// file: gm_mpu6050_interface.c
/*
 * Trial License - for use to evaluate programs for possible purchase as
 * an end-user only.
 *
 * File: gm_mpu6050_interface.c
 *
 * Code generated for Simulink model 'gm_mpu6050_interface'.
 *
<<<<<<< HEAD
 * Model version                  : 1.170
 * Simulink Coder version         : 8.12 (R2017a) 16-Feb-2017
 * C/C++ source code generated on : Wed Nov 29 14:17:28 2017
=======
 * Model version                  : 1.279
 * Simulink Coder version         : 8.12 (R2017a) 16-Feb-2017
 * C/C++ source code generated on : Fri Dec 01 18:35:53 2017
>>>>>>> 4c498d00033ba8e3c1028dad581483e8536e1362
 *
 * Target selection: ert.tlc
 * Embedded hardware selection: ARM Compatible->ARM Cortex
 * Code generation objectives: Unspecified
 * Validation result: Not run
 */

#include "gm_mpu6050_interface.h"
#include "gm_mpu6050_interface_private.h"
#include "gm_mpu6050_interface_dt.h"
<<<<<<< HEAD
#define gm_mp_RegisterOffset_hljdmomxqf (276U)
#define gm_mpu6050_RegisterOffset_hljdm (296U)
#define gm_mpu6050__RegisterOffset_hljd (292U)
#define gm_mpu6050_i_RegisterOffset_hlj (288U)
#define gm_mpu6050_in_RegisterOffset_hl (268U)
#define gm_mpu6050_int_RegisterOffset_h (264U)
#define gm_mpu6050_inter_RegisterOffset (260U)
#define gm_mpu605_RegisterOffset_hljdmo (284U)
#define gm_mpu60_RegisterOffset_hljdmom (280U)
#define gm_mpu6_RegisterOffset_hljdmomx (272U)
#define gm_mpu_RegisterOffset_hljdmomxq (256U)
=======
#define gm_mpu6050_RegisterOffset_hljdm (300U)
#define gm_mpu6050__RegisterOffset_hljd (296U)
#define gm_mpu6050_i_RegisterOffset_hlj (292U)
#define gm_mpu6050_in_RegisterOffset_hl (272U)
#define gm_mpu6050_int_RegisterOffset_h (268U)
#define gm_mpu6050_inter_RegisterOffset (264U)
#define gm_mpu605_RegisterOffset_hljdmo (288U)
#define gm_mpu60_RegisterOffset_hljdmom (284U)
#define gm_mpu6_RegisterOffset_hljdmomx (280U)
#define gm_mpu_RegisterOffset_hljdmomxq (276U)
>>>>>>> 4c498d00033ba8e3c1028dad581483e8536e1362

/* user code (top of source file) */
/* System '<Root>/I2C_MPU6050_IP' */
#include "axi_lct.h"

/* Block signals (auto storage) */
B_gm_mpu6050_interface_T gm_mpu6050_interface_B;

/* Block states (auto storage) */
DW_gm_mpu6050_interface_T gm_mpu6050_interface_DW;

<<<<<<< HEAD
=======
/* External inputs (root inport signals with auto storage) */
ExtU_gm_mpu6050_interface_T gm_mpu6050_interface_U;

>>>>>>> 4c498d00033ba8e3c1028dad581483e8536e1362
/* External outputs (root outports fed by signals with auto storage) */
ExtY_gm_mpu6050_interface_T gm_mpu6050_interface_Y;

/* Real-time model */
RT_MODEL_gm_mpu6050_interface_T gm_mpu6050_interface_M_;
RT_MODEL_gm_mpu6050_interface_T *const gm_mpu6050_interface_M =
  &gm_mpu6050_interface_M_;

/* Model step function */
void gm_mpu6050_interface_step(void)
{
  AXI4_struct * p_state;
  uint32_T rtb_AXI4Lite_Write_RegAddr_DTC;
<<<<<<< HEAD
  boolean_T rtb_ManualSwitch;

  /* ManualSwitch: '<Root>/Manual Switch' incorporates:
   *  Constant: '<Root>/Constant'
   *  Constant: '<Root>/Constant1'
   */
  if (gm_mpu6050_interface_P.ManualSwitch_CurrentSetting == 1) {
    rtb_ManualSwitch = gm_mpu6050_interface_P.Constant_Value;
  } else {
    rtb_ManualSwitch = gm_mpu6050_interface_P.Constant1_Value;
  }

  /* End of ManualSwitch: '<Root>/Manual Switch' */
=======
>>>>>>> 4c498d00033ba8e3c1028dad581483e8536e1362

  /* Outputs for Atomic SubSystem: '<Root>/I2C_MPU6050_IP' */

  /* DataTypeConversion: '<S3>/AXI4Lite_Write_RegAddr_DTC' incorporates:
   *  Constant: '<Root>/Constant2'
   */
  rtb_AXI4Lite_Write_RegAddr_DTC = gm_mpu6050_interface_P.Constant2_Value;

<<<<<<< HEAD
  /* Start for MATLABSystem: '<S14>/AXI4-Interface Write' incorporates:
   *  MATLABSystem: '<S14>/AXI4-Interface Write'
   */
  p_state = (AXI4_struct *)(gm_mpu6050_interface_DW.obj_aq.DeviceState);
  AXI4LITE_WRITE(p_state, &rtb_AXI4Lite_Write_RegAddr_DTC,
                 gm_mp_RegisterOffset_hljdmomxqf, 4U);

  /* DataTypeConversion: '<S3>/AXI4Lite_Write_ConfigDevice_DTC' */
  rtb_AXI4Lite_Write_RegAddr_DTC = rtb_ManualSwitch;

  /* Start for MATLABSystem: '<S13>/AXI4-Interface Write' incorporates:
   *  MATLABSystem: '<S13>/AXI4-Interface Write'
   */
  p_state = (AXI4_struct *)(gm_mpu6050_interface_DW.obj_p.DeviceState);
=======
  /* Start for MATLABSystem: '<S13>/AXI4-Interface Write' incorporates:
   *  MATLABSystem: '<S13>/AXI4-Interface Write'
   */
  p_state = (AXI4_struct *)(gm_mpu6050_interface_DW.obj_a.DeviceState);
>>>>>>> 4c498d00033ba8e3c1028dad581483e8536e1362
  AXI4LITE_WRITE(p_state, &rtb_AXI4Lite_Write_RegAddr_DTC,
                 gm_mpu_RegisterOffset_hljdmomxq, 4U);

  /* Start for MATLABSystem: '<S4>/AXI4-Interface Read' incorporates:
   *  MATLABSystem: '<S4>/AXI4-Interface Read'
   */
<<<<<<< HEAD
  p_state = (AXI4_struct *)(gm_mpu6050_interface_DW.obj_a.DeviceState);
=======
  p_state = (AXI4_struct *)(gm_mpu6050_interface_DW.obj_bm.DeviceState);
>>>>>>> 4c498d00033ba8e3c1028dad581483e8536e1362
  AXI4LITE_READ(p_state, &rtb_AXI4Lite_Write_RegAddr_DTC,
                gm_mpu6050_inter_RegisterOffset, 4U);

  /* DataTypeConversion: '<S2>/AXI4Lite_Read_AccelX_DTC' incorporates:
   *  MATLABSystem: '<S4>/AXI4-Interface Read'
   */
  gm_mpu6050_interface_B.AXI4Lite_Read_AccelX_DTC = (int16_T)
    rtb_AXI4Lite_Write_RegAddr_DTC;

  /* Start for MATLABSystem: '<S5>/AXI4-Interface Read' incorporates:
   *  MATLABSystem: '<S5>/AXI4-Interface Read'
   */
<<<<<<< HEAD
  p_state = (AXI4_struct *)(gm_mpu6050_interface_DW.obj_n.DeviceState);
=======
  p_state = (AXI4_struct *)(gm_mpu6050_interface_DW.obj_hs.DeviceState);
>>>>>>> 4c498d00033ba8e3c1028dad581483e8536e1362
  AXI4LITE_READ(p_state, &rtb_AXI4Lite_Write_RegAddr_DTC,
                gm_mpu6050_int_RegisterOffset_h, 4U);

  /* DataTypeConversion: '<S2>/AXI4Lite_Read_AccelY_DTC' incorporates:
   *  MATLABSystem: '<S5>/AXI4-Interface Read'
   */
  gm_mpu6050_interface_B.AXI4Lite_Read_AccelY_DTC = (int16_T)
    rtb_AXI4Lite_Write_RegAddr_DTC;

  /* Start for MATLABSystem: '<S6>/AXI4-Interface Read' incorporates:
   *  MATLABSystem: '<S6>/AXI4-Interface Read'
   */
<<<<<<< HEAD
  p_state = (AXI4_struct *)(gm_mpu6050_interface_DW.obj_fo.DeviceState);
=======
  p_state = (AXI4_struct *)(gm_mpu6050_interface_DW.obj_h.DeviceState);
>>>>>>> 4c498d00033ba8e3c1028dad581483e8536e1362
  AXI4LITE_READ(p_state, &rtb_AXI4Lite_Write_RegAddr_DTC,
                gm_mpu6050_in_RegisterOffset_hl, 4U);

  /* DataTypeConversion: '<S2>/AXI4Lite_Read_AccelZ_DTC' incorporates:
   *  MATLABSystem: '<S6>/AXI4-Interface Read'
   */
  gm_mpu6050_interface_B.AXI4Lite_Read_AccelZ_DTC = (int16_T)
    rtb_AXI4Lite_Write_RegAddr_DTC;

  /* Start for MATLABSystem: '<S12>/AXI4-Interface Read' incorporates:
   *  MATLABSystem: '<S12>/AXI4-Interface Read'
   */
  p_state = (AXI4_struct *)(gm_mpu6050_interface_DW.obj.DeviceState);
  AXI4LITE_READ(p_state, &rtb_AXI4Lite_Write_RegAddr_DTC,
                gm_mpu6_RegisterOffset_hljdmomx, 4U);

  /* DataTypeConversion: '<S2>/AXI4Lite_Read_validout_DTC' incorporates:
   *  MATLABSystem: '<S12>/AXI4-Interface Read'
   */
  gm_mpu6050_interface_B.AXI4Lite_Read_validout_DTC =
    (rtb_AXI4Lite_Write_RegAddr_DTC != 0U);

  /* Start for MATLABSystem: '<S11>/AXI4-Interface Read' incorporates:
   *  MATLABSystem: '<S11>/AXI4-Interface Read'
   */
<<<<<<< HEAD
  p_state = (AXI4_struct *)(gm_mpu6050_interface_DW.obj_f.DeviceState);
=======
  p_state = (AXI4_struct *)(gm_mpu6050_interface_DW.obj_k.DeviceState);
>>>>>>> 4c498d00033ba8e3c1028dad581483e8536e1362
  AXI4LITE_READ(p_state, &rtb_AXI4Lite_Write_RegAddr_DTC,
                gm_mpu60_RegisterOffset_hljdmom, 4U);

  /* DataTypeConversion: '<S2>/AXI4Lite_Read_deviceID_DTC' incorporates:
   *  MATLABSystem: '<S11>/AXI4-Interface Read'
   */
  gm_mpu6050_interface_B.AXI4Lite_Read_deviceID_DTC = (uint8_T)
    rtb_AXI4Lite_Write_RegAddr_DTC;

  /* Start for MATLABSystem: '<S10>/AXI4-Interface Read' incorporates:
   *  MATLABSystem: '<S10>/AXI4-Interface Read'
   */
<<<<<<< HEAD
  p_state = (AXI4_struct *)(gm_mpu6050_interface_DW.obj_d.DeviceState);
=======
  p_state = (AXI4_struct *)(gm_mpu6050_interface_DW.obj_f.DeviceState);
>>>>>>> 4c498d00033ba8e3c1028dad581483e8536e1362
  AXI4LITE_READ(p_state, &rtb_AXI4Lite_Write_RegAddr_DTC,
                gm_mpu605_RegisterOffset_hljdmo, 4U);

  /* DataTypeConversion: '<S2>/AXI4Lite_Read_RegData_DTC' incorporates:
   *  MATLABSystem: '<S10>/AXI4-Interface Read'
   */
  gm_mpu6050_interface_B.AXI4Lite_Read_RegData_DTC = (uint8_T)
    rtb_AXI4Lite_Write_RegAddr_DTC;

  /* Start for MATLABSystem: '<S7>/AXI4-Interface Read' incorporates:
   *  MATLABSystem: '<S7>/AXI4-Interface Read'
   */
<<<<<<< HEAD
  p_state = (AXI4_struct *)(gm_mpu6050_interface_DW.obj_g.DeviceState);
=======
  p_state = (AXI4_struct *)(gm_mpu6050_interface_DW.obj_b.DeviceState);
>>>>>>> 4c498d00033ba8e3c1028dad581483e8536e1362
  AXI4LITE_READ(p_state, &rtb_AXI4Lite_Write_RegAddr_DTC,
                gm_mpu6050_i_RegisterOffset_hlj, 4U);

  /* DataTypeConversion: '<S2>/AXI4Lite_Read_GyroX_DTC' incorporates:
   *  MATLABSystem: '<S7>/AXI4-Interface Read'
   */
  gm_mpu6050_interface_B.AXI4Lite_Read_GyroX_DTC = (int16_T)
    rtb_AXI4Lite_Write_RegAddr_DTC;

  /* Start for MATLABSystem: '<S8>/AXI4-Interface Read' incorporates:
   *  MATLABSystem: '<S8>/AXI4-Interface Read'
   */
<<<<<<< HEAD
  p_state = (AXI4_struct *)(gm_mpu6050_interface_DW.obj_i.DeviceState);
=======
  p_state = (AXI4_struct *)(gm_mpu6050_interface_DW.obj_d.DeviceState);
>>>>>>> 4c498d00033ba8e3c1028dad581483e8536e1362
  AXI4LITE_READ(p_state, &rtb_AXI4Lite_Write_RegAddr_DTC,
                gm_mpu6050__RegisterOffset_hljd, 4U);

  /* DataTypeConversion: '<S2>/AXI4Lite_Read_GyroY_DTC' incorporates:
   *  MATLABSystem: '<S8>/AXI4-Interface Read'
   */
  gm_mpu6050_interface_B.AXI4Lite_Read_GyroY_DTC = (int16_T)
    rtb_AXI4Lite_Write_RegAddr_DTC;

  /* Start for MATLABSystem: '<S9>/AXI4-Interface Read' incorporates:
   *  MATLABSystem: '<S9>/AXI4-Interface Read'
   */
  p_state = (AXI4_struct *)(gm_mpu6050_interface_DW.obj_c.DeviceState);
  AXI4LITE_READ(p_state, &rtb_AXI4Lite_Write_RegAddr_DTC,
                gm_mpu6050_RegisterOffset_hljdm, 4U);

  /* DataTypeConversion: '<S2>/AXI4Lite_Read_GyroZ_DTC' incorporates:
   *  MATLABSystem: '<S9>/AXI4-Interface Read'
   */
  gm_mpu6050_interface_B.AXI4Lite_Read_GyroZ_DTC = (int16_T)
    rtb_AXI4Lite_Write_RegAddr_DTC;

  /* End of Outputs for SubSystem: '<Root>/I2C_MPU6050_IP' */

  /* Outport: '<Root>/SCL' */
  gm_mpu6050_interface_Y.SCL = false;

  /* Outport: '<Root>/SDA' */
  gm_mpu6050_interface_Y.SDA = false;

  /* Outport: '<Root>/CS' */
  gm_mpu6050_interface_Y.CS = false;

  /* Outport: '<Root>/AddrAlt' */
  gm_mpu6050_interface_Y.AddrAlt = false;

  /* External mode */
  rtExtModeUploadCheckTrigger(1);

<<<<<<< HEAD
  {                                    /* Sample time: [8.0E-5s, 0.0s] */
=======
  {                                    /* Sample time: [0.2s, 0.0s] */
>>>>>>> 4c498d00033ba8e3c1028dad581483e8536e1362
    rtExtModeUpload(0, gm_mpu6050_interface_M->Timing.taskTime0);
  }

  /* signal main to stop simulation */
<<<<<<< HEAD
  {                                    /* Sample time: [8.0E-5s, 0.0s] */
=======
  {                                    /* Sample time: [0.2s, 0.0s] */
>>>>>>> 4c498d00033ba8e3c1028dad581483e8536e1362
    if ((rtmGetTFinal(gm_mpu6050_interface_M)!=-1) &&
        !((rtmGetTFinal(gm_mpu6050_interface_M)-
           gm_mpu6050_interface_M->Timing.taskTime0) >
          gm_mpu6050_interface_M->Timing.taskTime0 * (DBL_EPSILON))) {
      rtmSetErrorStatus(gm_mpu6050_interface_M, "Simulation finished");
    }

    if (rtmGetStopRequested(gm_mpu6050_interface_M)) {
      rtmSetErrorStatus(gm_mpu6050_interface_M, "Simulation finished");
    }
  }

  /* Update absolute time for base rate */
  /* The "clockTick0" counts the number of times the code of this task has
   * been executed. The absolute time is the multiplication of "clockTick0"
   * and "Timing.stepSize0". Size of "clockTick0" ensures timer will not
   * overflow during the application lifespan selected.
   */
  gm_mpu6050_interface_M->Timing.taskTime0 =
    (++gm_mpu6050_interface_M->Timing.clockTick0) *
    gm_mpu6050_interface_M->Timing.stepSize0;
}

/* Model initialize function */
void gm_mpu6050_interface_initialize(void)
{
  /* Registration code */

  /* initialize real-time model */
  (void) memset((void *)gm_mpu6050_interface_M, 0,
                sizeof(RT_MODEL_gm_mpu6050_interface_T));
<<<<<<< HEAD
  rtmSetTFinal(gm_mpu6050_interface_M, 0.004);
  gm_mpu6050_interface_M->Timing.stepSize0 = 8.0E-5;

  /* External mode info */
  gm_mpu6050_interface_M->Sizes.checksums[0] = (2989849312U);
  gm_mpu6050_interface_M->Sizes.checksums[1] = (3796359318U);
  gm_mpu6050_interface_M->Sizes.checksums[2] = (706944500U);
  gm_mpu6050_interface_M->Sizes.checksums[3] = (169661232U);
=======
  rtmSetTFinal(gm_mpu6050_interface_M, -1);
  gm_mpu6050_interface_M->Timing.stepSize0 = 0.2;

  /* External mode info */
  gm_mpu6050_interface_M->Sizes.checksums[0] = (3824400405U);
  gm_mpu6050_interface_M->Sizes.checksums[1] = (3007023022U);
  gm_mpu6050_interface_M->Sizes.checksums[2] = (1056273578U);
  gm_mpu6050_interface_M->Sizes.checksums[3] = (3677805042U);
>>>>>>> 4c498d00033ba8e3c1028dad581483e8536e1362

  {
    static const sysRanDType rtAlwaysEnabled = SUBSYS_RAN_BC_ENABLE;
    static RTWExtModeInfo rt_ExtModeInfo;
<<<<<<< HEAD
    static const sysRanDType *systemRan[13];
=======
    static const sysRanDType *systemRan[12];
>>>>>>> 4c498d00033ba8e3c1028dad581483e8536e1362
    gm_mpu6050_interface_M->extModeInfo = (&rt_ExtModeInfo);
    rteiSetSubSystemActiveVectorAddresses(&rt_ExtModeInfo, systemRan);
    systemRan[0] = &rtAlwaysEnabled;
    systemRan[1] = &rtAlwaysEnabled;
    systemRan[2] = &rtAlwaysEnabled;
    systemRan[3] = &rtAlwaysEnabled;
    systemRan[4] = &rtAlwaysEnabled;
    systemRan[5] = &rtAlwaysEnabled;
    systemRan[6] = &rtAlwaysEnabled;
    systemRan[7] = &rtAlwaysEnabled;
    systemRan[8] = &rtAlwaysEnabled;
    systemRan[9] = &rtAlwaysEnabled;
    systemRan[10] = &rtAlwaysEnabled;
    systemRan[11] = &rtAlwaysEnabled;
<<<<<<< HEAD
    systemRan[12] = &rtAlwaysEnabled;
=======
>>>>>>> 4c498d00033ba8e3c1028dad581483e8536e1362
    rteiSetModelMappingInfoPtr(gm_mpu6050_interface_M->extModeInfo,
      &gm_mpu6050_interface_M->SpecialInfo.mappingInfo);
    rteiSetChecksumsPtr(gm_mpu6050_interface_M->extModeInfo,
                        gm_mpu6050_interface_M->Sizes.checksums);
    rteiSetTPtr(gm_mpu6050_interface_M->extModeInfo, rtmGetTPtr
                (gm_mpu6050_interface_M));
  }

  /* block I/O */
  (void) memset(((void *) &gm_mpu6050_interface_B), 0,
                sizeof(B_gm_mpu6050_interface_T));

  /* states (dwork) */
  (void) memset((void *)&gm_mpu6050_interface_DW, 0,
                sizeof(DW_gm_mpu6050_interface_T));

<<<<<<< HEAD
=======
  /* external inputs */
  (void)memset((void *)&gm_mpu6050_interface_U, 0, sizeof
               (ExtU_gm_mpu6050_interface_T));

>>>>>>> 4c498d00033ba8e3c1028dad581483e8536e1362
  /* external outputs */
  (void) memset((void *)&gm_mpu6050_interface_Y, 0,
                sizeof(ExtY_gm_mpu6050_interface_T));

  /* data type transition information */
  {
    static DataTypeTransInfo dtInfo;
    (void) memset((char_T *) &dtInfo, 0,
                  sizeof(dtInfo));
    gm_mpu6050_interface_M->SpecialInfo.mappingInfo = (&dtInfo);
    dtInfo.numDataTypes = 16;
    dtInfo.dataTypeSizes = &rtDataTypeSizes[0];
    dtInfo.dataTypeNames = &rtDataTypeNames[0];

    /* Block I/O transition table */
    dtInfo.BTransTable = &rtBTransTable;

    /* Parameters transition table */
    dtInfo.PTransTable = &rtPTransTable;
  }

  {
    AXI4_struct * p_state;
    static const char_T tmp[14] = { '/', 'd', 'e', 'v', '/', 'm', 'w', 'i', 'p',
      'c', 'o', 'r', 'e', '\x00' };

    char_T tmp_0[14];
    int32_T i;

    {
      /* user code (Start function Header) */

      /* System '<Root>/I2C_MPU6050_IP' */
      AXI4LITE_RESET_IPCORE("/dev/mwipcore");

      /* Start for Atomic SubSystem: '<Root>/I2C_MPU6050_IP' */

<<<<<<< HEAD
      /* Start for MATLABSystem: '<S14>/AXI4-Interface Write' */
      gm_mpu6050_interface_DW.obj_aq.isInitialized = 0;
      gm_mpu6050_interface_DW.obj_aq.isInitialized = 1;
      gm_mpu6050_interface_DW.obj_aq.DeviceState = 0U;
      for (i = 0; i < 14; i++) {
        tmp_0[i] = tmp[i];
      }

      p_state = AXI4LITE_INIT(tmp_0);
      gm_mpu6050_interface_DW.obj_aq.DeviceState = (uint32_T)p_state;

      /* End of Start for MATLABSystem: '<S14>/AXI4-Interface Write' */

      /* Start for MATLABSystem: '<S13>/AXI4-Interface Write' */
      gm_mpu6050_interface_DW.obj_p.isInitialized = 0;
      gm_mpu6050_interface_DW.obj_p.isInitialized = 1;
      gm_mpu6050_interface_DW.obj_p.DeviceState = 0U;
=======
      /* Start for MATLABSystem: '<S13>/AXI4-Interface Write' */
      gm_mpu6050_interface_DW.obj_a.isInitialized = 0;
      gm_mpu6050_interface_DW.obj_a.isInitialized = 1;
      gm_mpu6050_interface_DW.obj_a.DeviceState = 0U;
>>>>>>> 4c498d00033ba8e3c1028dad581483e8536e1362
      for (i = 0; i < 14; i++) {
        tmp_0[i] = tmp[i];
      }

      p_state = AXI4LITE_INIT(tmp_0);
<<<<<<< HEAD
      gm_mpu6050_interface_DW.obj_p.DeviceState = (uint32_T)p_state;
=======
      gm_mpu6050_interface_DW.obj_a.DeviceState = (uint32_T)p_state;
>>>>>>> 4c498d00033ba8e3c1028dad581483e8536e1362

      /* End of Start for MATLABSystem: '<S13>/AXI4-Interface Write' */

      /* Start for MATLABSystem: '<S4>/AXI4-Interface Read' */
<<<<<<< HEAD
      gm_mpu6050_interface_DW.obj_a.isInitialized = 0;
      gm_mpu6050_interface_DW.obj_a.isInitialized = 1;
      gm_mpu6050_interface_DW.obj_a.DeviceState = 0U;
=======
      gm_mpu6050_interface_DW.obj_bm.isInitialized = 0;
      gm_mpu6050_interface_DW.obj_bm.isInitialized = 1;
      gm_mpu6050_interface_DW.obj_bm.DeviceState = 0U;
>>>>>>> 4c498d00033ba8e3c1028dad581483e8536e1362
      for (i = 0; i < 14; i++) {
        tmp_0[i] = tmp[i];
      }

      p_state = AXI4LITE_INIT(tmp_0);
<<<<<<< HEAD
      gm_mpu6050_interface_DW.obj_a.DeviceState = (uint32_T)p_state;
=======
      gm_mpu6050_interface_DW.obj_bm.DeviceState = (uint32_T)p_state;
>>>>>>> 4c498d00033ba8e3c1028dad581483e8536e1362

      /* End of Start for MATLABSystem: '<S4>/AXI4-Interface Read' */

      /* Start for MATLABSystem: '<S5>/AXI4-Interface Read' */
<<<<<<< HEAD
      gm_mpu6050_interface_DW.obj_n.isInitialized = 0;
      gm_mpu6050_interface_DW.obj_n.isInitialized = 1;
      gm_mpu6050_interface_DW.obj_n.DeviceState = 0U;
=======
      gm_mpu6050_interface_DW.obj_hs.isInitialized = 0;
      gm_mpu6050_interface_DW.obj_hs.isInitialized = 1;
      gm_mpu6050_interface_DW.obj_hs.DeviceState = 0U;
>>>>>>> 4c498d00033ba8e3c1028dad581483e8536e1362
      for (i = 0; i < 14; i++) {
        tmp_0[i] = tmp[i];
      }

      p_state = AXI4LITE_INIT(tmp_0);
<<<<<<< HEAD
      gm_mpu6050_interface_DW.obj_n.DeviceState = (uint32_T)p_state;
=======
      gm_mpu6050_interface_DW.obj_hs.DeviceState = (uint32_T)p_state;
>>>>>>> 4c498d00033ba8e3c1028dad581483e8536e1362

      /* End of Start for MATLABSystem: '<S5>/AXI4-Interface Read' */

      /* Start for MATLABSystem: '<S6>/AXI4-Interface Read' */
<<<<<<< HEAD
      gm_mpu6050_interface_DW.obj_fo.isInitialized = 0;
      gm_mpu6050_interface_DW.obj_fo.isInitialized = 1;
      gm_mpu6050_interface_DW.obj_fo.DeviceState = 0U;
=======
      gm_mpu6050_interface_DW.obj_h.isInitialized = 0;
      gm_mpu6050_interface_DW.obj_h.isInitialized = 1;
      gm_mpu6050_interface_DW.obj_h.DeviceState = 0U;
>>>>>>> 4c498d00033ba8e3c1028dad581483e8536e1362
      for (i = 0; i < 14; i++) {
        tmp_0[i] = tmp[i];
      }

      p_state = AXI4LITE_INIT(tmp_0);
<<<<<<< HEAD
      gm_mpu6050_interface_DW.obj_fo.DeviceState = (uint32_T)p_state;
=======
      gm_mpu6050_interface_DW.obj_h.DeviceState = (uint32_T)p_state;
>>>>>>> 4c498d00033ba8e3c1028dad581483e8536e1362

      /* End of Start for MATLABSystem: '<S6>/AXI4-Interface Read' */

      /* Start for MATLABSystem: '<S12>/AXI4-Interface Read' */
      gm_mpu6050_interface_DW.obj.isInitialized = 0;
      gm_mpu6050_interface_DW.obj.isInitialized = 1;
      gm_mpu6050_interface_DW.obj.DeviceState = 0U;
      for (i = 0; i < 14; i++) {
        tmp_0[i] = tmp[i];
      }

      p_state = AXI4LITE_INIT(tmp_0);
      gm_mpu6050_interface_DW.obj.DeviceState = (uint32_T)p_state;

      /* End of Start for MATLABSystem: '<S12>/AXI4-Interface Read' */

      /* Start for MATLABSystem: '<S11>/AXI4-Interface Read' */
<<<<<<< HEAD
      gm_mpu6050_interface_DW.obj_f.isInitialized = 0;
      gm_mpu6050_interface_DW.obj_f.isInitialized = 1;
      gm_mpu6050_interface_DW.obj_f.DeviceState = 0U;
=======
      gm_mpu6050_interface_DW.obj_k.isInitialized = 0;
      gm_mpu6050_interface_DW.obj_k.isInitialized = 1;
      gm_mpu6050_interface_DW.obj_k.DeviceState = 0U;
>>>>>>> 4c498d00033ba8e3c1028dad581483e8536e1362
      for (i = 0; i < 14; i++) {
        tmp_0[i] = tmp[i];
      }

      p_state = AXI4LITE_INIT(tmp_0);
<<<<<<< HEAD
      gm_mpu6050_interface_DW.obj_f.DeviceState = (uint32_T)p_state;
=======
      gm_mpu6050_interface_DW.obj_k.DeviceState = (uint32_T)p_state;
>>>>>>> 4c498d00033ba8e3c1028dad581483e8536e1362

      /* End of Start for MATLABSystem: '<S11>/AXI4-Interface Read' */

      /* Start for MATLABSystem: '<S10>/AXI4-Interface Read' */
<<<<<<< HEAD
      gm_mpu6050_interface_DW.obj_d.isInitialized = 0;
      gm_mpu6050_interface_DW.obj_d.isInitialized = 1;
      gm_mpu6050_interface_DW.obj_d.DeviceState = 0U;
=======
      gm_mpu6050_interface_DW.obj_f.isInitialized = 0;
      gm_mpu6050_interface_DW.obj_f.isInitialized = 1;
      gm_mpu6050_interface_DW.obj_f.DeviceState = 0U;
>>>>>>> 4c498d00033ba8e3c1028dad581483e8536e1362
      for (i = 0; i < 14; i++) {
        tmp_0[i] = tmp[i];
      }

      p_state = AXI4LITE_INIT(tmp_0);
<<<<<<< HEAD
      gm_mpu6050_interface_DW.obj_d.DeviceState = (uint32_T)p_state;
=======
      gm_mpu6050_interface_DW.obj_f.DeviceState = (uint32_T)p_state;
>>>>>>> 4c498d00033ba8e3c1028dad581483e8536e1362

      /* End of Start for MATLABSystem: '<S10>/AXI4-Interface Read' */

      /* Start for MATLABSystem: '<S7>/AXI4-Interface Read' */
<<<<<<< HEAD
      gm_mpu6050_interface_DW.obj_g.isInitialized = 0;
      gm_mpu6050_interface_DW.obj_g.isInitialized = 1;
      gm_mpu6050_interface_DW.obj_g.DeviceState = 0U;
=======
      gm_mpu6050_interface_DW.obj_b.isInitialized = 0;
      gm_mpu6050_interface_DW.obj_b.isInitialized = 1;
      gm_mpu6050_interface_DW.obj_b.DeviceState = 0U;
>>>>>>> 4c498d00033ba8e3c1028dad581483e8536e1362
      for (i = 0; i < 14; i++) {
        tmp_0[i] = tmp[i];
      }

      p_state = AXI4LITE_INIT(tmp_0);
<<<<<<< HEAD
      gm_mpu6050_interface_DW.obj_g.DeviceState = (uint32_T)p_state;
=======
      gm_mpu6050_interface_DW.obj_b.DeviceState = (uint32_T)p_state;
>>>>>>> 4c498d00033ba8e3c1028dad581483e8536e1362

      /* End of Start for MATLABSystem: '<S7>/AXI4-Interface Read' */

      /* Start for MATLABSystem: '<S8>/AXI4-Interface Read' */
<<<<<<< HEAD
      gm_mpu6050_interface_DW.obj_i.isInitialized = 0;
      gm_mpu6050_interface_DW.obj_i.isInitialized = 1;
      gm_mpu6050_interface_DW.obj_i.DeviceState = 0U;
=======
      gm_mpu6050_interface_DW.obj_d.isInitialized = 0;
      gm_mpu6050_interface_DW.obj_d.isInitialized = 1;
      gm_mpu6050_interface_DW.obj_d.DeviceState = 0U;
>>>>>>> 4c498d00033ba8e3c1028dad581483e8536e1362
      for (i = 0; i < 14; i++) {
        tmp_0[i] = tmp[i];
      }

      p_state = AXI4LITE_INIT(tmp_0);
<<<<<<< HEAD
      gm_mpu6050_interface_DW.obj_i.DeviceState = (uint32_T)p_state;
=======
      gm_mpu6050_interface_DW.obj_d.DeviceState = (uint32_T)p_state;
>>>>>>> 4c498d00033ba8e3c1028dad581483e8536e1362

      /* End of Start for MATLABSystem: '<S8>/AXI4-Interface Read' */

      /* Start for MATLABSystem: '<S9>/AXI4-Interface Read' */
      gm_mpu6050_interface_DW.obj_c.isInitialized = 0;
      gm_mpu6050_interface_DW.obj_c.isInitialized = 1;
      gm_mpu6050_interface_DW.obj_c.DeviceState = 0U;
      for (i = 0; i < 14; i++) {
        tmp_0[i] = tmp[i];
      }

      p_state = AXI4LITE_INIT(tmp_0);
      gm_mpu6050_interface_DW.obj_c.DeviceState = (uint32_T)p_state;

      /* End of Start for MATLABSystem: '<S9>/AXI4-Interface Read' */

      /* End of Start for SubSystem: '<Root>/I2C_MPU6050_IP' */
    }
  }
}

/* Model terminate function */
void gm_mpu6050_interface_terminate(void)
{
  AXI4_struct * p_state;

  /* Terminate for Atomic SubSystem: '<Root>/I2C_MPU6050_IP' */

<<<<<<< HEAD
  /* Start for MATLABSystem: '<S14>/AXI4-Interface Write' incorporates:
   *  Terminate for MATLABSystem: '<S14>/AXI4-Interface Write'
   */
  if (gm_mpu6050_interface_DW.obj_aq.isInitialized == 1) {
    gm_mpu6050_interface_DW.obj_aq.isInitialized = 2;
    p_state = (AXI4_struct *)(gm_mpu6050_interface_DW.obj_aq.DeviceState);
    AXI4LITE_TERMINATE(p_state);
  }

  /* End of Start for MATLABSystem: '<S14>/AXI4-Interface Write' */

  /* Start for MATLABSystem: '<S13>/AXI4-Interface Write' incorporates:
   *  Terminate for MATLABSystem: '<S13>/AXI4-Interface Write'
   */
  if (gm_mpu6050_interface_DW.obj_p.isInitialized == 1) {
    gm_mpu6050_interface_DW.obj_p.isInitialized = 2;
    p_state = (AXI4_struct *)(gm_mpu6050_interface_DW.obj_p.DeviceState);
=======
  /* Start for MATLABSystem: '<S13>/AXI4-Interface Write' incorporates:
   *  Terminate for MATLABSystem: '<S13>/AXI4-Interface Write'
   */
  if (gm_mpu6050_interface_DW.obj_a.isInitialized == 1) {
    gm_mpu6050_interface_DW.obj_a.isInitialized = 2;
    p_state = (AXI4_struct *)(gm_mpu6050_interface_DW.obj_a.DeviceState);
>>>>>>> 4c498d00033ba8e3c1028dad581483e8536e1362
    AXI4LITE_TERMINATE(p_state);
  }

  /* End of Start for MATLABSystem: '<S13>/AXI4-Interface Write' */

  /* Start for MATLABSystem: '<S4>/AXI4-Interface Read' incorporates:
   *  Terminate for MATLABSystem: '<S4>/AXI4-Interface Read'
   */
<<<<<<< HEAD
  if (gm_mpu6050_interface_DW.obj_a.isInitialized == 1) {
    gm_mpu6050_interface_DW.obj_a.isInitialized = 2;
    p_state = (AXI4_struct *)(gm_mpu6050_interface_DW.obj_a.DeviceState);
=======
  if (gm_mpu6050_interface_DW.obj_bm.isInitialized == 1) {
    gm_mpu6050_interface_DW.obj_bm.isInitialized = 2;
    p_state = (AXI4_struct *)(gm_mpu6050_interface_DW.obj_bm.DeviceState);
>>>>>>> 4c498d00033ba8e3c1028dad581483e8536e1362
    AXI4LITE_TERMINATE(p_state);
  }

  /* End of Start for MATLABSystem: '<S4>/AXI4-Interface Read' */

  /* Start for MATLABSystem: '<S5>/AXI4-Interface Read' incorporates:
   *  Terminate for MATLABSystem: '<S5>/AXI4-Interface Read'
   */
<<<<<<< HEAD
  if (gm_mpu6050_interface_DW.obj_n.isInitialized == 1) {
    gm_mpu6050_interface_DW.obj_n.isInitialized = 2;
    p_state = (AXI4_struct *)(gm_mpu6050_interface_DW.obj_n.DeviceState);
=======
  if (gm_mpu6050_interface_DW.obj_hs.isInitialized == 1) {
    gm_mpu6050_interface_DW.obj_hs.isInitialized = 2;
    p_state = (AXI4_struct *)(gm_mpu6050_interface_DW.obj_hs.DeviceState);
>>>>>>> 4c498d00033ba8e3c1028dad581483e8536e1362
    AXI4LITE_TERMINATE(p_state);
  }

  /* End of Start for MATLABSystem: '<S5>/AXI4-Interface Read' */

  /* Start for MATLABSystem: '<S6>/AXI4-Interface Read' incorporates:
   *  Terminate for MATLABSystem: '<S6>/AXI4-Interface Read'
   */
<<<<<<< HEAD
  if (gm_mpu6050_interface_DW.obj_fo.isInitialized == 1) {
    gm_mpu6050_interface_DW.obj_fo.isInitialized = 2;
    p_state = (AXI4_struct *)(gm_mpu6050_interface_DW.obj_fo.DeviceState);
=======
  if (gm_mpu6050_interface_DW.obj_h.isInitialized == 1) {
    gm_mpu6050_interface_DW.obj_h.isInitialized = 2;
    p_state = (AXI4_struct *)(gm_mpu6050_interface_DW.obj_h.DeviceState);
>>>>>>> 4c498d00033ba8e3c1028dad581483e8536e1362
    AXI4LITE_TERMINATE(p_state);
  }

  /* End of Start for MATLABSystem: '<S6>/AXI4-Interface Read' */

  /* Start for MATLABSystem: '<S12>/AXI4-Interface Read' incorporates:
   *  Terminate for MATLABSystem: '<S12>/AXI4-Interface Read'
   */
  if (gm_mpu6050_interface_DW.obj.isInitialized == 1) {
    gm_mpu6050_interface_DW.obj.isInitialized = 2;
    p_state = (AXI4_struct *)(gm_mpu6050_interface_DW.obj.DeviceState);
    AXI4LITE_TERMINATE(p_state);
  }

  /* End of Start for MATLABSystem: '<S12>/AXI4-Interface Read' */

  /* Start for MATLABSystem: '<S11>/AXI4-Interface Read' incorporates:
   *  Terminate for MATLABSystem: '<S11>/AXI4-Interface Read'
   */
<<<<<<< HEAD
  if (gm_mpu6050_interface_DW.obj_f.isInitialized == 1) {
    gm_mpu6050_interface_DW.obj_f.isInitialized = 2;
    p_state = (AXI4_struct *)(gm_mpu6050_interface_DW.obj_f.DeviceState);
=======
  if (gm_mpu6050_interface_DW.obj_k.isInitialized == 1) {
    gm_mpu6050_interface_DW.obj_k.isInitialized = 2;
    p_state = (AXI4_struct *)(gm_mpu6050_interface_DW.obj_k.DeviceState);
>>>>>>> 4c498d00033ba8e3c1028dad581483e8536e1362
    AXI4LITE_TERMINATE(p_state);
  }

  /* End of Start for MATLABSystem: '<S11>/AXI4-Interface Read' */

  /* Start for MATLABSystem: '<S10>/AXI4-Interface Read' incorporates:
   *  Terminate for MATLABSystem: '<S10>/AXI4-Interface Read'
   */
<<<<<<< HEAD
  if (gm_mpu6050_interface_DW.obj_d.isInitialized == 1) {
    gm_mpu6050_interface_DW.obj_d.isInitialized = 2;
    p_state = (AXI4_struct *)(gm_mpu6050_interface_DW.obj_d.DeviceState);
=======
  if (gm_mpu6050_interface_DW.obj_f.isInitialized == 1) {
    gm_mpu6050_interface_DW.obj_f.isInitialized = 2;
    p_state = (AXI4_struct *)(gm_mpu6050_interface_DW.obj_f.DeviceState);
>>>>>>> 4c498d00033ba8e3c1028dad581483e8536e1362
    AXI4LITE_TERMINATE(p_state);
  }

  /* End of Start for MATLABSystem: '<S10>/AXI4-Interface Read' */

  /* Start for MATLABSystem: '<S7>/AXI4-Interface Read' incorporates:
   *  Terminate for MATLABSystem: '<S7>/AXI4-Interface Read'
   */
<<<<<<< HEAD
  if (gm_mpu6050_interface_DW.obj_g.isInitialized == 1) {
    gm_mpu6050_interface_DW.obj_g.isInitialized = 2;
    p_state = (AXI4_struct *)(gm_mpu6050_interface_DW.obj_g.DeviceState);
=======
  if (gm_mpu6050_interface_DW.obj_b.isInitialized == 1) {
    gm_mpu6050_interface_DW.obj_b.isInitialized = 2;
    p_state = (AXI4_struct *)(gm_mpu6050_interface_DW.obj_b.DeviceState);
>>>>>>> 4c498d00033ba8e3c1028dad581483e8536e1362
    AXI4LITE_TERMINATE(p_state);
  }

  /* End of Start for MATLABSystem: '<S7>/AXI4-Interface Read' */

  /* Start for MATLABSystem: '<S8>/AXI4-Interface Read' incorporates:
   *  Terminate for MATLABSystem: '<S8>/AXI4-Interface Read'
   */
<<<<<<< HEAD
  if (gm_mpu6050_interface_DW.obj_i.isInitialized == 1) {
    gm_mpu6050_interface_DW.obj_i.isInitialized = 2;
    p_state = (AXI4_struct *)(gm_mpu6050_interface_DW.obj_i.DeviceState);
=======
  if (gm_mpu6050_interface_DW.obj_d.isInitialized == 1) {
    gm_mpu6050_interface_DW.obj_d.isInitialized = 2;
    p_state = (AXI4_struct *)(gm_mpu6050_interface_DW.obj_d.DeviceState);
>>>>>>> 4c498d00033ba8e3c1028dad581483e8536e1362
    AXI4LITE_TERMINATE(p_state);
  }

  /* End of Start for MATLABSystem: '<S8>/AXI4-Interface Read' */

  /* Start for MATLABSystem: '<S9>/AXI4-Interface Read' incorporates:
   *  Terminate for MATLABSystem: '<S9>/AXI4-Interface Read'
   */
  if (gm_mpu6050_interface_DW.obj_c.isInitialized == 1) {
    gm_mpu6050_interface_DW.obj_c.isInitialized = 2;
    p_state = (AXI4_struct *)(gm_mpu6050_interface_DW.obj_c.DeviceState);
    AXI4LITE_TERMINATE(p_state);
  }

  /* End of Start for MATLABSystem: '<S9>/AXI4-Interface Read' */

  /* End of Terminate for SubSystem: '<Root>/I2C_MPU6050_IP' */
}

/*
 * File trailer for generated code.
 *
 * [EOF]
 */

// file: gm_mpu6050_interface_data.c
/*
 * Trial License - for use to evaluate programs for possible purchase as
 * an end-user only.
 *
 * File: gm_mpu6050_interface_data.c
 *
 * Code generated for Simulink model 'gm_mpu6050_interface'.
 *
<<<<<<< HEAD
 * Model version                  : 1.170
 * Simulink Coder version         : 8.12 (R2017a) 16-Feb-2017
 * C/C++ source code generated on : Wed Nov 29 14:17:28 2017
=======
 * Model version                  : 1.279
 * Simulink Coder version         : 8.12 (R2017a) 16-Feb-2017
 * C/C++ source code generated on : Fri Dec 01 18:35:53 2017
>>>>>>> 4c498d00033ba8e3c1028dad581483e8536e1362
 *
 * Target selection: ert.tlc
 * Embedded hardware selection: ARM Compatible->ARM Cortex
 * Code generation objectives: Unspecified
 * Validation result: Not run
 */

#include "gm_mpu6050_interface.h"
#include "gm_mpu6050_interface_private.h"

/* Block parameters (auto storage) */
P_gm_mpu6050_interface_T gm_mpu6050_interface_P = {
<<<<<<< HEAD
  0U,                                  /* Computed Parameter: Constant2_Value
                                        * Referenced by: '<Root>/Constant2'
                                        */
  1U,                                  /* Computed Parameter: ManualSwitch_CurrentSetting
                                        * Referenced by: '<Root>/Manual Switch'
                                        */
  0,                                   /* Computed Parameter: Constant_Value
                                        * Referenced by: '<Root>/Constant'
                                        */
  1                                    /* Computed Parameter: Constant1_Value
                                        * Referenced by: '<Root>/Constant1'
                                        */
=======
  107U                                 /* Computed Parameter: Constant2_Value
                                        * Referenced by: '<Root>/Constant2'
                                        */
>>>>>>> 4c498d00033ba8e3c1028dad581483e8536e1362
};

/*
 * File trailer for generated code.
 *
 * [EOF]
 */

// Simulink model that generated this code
simulink model "gm_mpu6050_interface"  (R2017a)
settings: Solver=FixedStepDiscrete  StartTime=0.0  StopTime=0.004  RelTol=1e-3  EnableMultiTasking=on
PostLoadFcn:
  | ChipSelect = 1;  % choose I2C comms
  | AddressAlt  = 0;  % use default address
  | 
  | if AddressAlt == 1
  | % b1101001 (pin AD0 is logic high).
  | SlvAddr = uint8(bin2dec('1101001'));  % ADDR ALT = 1
  | else
  | % b1101000 (pin AD0 is logic low)
  | SlvAddr = uint8(bin2dec('1101000'));  % ADDR ALT = 0
  | end
  | 
  | % 0x3B 59 ACCEL_XOUT[15:8]
  | % 0x3C 60 ACCEL_XOUT[7:0]
  | % 0x3D 61 ACCEL_YOUT[15:8]
  | % 0x3E 62 ACCEL_YOUT[7:0]
  | % 0x3F 63 ACCEL_ZOUT[15:8]
  | % 0x40 64 ACCEL_ZOUT[7:0]
  | 
  | AccelXRegAddr = uint8(hex2dec('3B'));
  | AccelYRegAddr = uint8(hex2dec('3D'));
  | AccelZRegAddr = uint8(hex2dec('3F'));
  | 
  | % 0x43 67 GYRO_XOUT[15:8]
  | % 0x44 68 GYRO_XOUT[7:0]
  | % 0x45 69 GYRO_YOUT[15:8]
  | % 0x46 70 GYRO_YOUT[7:0]
  | % 0x47 71 GYRO_ZOUT[15:8]
  | % 0x48 72 GYRO_ZOUT[7:0]
  | 
  | GyroXRegAddr = uint8(hex2dec('43'));
  | GyroYRegAddr = uint8(hex2dec('45'));
  | GyroZRegAddr = uint8(hex2dec('47'));
  | 
  | deviceAddr = fi(SlvAddr,0,7,0);
  | 
  | powerRegAddr = uint8(hex2dec('6B'));
  | powerRegData = bin2dec('10000001');
undefined symbols (not defined in the file or in its folder): AXI4, Lite
libraries: axiinterfacelib x11

== system gm_mpu6050_interface ==
  note: Generated by HDL Workflow Advisor on 18-Nov-2017 14:43:12
  Constant : Constant  Value=0  OutDataTypeStr=boolean  SampleTime=-1
  Constant1 : Constant  OutDataTypeStr=boolean  SampleTime=-1
  Constant2 : Constant  Value=0  OutDataTypeStr=uint8  SampleTime=-1
  I2C_MPU6050_IP : Subsystem  TreatAsAtomicUnit=on  mask(AXI4-Lite/AXI4 Interface){}
      mask help:
      | This is an automatically generated subsystem block.
      | This contains the AXI interface blocks that communicate with the I2C_MPU60_ip IPCore generated from mpu6050/I2C_MPU6050_IP subsystem.
  Manual Switch : ManualSwitch
  Mux : Mux  Inputs=3
  Mux1 : Mux  Inputs=3
  Scope : Scope  NumInputPorts=2
  Scope1 : Scope  NumInputPorts=2
  UserRegValue : Display
  deviceID : Display
  SCL : Outport
  SDA : Outport  Port=2
  CS : Outport  Port=3
  AddrAlt : Outport  Port=4
  wires:
  I2C_MPU6050_IP/6(validout) -> Scope1/2, Scope/2
  I2C_MPU6050_IP/12(GyroY) -> Mux1/2
  I2C_MPU6050_IP/11(GyroX) -> Mux1/1
  I2C_MPU6050_IP/13(GyroZ) -> Mux1/3
  Mux1/1 -> Scope1/1
  Constant2/1 -> I2C_MPU6050_IP/1(RegAddr)
  Manual Switch/1 -> I2C_MPU6050_IP/2(ConfigDevice)
  Constant1/1 -> Manual Switch/2
  Constant/1 -> Manual Switch/1
  Mux/1 -> Scope/1
  I2C_MPU6050_IP/10(RegData) -> UserRegValue/1
  I2C_MPU6050_IP/7(deviceID) -> deviceID/1
  I2C_MPU6050_IP/5(AccelZ) -> Mux/3
  I2C_MPU6050_IP/3(AccelX) -> Mux/1
  I2C_MPU6050_IP/4(AccelY) -> Mux/2
  I2C_MPU6050_IP/9(ADDRALT) -> AddrAlt/1
  I2C_MPU6050_IP/8(CS) -> CS/1
  I2C_MPU6050_IP/1(SCL) -> SCL/1
  I2C_MPU6050_IP/2(SDA) -> SDA/1

== system gm_mpu6050_interface/I2C_MPU6050_IP ==
  note: Generated by HDL Workflow Advisor on 18-Nov-2017 14:43:12
  RegAddr : Inport
  ConfigDevice : Inport  Port=2
  AXI4LiteRead : Subsystem  Priority=10
  AXI4LiteWrite : Subsystem  Priority=1
  AXI4Reset : Subsystem  mask(System Start){ShowInLibBrowser=0}
      mask prompts: ShowInLibBrowser "Simulink:masks:CustCodeMaskParam1_MP"
  AXI4ResetModelSource : Subsystem  mask(Model Source){ShowInLibBrowser=0}
      mask prompts: ShowInLibBrowser "Simulink:masks:CustCodeMaskParam1_MP"
  SCL : Outport
  SDA : Outport  Port=2
  AccelX : Outport  Port=3
  AccelY : Outport  Port=4
  AccelZ : Outport  Port=5
  validout : Outport  Port=6
  deviceID : Outport  Port=7
  CS : Outport  Port=8
  ADDRALT : Outport  Port=9
  RegData : Outport  Port=10
  GyroX : Outport  Port=11
  GyroY : Outport  Port=12
  GyroZ : Outport  Port=13
  wires:
  RegAddr/1 -> AXI4LiteWrite/1(In1)
  ConfigDevice/1 -> AXI4LiteWrite/2(In2)
  AXI4LiteRead/1(Out1) -> CS/1
  AXI4LiteRead/2(Out2) -> ADDRALT/1
  AXI4LiteRead/3(Out3) -> SCL/1
  AXI4LiteRead/4(Out4) -> SDA/1
  AXI4LiteRead/5(Out5) -> AccelX/1
  AXI4LiteRead/6(Out6) -> AccelY/1
  AXI4LiteRead/7(Out7) -> AccelZ/1
  AXI4LiteRead/8(Out8) -> validout/1
  AXI4LiteRead/9(Out9) -> deviceID/1
  AXI4LiteRead/10(Out10) -> RegData/1
  AXI4LiteRead/11(Out11) -> GyroX/1
  AXI4LiteRead/12(Out12) -> GyroY/1
  AXI4LiteRead/13(Out13) -> GyroZ/1

== system gm_mpu6050_interface/I2C_MPU6050_IP/AXI4LiteRead ==
  AXI4Lite_Read_AccelX : axiinterfacelib/AXI4-Interface Read  Priority=4  AXIInterfaceType=AXI4-Lite  DeviceName=/dev/mwipcore  RegisterOffset=hex2dec('104')  DataLength=1  DataType=uint32  SampleTime=-1  blockPlatform=ZYNQ  SimulateUsing=Interpreted Execution
  AXI4Lite_Read_AccelX_DTC : DataTypeConversion  OutDataTypeStr=fixdt('int16')  ConvertRealWorld=Stored Integer (SI)
  AXI4Lite_Read_AccelY : axiinterfacelib/AXI4-Interface Read  Priority=5  AXIInterfaceType=AXI4-Lite  DeviceName=/dev/mwipcore  RegisterOffset=hex2dec('108')  DataLength=1  DataType=uint32  SampleTime=-1  blockPlatform=ZYNQ  SimulateUsing=Interpreted Execution
  AXI4Lite_Read_AccelY_DTC : DataTypeConversion  OutDataTypeStr=fixdt('int16')  ConvertRealWorld=Stored Integer (SI)
  AXI4Lite_Read_AccelZ : axiinterfacelib/AXI4-Interface Read  Priority=6  AXIInterfaceType=AXI4-Lite  DeviceName=/dev/mwipcore  RegisterOffset=hex2dec('10C')  DataLength=1  DataType=uint32  SampleTime=-1  blockPlatform=ZYNQ  SimulateUsing=Interpreted Execution
  AXI4Lite_Read_AccelZ_DTC : DataTypeConversion  OutDataTypeStr=fixdt('int16')  ConvertRealWorld=Stored Integer (SI)
  AXI4Lite_Read_GyroX : axiinterfacelib/AXI4-Interface Read  Priority=12  AXIInterfaceType=AXI4-Lite  DeviceName=/dev/mwipcore  RegisterOffset=hex2dec('120')  DataLength=1  DataType=uint32  SampleTime=-1  blockPlatform=ZYNQ  SimulateUsing=Interpreted Execution
  AXI4Lite_Read_GyroX_DTC : DataTypeConversion  OutDataTypeStr=fixdt('int16')  ConvertRealWorld=Stored Integer (SI)
  AXI4Lite_Read_GyroY : axiinterfacelib/AXI4-Interface Read  Priority=13  AXIInterfaceType=AXI4-Lite  DeviceName=/dev/mwipcore  RegisterOffset=hex2dec('124')  DataLength=1  DataType=uint32  SampleTime=-1  blockPlatform=ZYNQ  SimulateUsing=Interpreted Execution
  AXI4Lite_Read_GyroY_DTC : DataTypeConversion  OutDataTypeStr=fixdt('int16')  ConvertRealWorld=Stored Integer (SI)
  AXI4Lite_Read_GyroZ : axiinterfacelib/AXI4-Interface Read  Priority=14  AXIInterfaceType=AXI4-Lite  DeviceName=/dev/mwipcore  RegisterOffset=hex2dec('128')  DataLength=1  DataType=uint32  SampleTime=-1  blockPlatform=ZYNQ  SimulateUsing=Interpreted Execution
  AXI4Lite_Read_GyroZ_DTC : DataTypeConversion  OutDataTypeStr=fixdt('int16')  ConvertRealWorld=Stored Integer (SI)
  AXI4Lite_Read_RegData : axiinterfacelib/AXI4-Interface Read  Priority=11  AXIInterfaceType=AXI4-Lite  DeviceName=/dev/mwipcore  RegisterOffset=hex2dec('11C')  DataLength=1  DataType=uint32  SampleTime=-1  blockPlatform=ZYNQ  SimulateUsing=Interpreted Execution
  AXI4Lite_Read_RegData_DTC : DataTypeConversion  OutDataTypeStr=fixdt('uint8')  ConvertRealWorld=Stored Integer (SI)
  AXI4Lite_Read_deviceID : axiinterfacelib/AXI4-Interface Read  Priority=8  AXIInterfaceType=AXI4-Lite  DeviceName=/dev/mwipcore  RegisterOffset=hex2dec('118')  DataLength=1  DataType=uint32  SampleTime=-1  blockPlatform=ZYNQ  SimulateUsing=Interpreted Execution
  AXI4Lite_Read_deviceID_DTC : DataTypeConversion  OutDataTypeStr=fixdt('uint8')  ConvertRealWorld=Stored Integer (SI)
  AXI4Lite_Read_validout : axiinterfacelib/AXI4-Interface Read  Priority=7  AXIInterfaceType=AXI4-Lite  DeviceName=/dev/mwipcore  RegisterOffset=hex2dec('110')  DataLength=1  DataType=uint32  SampleTime=-1  blockPlatform=ZYNQ  SimulateUsing=Interpreted Execution
  AXI4Lite_Read_validout_DTC : DataTypeConversion  OutDataTypeStr=fixdt('boolean')  ConvertRealWorld=Stored Integer (SI)
  EXTERNALPORT_ADDRALT_DTC : DataTypeConversion  OutDataTypeStr=fixdt('boolean')
  EXTERNALPORT_CS_DTC : DataTypeConversion  OutDataTypeStr=fixdt('boolean')
  EXTERNALPORT_SCL_DTC : DataTypeConversion  OutDataTypeStr=fixdt('boolean')
  EXTERNALPORT_SDA_DTC : DataTypeConversion  OutDataTypeStr=fixdt('boolean')
  GROUND_ADDRALT : Ground
  GROUND_CS : Ground
  GROUND_SCL : Ground
  GROUND_SDA : Ground
  Out1 : Outport
  Out2 : Outport  Port=2
  Out3 : Outport  Port=3
  Out4 : Outport  Port=4
  Out5 : Outport  Port=5
  Out6 : Outport  Port=6
  Out7 : Outport  Port=7
  Out8 : Outport  Port=8
  Out9 : Outport  Port=9
  Out10 : Outport  Port=10
  Out11 : Outport  Port=11
  Out12 : Outport  Port=12
  Out13 : Outport  Port=13
  wires:
  EXTERNALPORT_SCL_DTC/1 -> Out3/1
  GROUND_SCL/1 -> EXTERNALPORT_SCL_DTC/1
  GROUND_SDA/1 -> EXTERNALPORT_SDA_DTC/1
  EXTERNALPORT_SDA_DTC/1 -> Out4/1
  AXI4Lite_Read_AccelZ/1 -> AXI4Lite_Read_AccelZ_DTC/1
  AXI4Lite_Read_AccelZ_DTC/1 -> Out7/1
  AXI4Lite_Read_deviceID/1 -> AXI4Lite_Read_deviceID_DTC/1
  AXI4Lite_Read_deviceID_DTC/1 -> Out9/1
  GROUND_ADDRALT/1 -> EXTERNALPORT_ADDRALT_DTC/1
  GROUND_CS/1 -> EXTERNALPORT_CS_DTC/1
  EXTERNALPORT_CS_DTC/1 -> Out1/1
  EXTERNALPORT_ADDRALT_DTC/1 -> Out2/1
  AXI4Lite_Read_GyroZ/1 -> AXI4Lite_Read_GyroZ_DTC/1
  AXI4Lite_Read_GyroZ_DTC/1 -> Out13/1
  AXI4Lite_Read_AccelY/1 -> AXI4Lite_Read_AccelY_DTC/1
  AXI4Lite_Read_validout_DTC/1 -> Out8/1
  AXI4Lite_Read_validout/1 -> AXI4Lite_Read_validout_DTC/1
  AXI4Lite_Read_AccelY_DTC/1 -> Out6/1
  AXI4Lite_Read_AccelX/1 -> AXI4Lite_Read_AccelX_DTC/1
  AXI4Lite_Read_AccelX_DTC/1 -> Out5/1
  AXI4Lite_Read_RegData/1 -> AXI4Lite_Read_RegData_DTC/1
  AXI4Lite_Read_GyroX_DTC/1 -> Out11/1
  AXI4Lite_Read_GyroY/1 -> AXI4Lite_Read_GyroY_DTC/1
  AXI4Lite_Read_GyroX/1 -> AXI4Lite_Read_GyroX_DTC/1
  AXI4Lite_Read_RegData_DTC/1 -> Out10/1
  AXI4Lite_Read_GyroY_DTC/1 -> Out12/1

== system gm_mpu6050_interface/I2C_MPU6050_IP/AXI4LiteWrite ==
  In1 : Inport
  In2 : Inport  Port=2
  AXI4Lite_Write_ConfigDevice : axiinterfacelib/AXI4-Interface Write  Priority=2  AXIInterfaceType=AXI4-Lite  DeviceName=/dev/mwipcore  RegisterOffset=hex2dec('100')  blockPlatform=ZYNQ  SimulateUsing=Interpreted execution
  AXI4Lite_Write_ConfigDevice_DTC : DataTypeConversion  OutDataTypeStr=uint32  ConvertRealWorld=Stored Integer (SI)
  AXI4Lite_Write_RegAddr : axiinterfacelib/AXI4-Interface Write  Priority=1  AXIInterfaceType=AXI4-Lite  DeviceName=/dev/mwipcore  RegisterOffset=hex2dec('114')  blockPlatform=ZYNQ  SimulateUsing=Interpreted execution
  AXI4Lite_Write_RegAddr_DTC : DataTypeConversion  OutDataTypeStr=uint32  ConvertRealWorld=Stored Integer (SI)
  wires:
  AXI4Lite_Write_ConfigDevice_DTC/1 -> AXI4Lite_Write_ConfigDevice/1
  In2/1 -> AXI4Lite_Write_ConfigDevice_DTC/1
  AXI4Lite_Write_RegAddr_DTC/1 -> AXI4Lite_Write_RegAddr/1
  In1/1 -> AXI4Lite_Write_RegAddr_DTC/1

== system gm_mpu6050_interface/I2C_MPU6050_IP/AXI4Reset ==

== system gm_mpu6050_interface/I2C_MPU6050_IP/AXI4ResetModelSource ==
